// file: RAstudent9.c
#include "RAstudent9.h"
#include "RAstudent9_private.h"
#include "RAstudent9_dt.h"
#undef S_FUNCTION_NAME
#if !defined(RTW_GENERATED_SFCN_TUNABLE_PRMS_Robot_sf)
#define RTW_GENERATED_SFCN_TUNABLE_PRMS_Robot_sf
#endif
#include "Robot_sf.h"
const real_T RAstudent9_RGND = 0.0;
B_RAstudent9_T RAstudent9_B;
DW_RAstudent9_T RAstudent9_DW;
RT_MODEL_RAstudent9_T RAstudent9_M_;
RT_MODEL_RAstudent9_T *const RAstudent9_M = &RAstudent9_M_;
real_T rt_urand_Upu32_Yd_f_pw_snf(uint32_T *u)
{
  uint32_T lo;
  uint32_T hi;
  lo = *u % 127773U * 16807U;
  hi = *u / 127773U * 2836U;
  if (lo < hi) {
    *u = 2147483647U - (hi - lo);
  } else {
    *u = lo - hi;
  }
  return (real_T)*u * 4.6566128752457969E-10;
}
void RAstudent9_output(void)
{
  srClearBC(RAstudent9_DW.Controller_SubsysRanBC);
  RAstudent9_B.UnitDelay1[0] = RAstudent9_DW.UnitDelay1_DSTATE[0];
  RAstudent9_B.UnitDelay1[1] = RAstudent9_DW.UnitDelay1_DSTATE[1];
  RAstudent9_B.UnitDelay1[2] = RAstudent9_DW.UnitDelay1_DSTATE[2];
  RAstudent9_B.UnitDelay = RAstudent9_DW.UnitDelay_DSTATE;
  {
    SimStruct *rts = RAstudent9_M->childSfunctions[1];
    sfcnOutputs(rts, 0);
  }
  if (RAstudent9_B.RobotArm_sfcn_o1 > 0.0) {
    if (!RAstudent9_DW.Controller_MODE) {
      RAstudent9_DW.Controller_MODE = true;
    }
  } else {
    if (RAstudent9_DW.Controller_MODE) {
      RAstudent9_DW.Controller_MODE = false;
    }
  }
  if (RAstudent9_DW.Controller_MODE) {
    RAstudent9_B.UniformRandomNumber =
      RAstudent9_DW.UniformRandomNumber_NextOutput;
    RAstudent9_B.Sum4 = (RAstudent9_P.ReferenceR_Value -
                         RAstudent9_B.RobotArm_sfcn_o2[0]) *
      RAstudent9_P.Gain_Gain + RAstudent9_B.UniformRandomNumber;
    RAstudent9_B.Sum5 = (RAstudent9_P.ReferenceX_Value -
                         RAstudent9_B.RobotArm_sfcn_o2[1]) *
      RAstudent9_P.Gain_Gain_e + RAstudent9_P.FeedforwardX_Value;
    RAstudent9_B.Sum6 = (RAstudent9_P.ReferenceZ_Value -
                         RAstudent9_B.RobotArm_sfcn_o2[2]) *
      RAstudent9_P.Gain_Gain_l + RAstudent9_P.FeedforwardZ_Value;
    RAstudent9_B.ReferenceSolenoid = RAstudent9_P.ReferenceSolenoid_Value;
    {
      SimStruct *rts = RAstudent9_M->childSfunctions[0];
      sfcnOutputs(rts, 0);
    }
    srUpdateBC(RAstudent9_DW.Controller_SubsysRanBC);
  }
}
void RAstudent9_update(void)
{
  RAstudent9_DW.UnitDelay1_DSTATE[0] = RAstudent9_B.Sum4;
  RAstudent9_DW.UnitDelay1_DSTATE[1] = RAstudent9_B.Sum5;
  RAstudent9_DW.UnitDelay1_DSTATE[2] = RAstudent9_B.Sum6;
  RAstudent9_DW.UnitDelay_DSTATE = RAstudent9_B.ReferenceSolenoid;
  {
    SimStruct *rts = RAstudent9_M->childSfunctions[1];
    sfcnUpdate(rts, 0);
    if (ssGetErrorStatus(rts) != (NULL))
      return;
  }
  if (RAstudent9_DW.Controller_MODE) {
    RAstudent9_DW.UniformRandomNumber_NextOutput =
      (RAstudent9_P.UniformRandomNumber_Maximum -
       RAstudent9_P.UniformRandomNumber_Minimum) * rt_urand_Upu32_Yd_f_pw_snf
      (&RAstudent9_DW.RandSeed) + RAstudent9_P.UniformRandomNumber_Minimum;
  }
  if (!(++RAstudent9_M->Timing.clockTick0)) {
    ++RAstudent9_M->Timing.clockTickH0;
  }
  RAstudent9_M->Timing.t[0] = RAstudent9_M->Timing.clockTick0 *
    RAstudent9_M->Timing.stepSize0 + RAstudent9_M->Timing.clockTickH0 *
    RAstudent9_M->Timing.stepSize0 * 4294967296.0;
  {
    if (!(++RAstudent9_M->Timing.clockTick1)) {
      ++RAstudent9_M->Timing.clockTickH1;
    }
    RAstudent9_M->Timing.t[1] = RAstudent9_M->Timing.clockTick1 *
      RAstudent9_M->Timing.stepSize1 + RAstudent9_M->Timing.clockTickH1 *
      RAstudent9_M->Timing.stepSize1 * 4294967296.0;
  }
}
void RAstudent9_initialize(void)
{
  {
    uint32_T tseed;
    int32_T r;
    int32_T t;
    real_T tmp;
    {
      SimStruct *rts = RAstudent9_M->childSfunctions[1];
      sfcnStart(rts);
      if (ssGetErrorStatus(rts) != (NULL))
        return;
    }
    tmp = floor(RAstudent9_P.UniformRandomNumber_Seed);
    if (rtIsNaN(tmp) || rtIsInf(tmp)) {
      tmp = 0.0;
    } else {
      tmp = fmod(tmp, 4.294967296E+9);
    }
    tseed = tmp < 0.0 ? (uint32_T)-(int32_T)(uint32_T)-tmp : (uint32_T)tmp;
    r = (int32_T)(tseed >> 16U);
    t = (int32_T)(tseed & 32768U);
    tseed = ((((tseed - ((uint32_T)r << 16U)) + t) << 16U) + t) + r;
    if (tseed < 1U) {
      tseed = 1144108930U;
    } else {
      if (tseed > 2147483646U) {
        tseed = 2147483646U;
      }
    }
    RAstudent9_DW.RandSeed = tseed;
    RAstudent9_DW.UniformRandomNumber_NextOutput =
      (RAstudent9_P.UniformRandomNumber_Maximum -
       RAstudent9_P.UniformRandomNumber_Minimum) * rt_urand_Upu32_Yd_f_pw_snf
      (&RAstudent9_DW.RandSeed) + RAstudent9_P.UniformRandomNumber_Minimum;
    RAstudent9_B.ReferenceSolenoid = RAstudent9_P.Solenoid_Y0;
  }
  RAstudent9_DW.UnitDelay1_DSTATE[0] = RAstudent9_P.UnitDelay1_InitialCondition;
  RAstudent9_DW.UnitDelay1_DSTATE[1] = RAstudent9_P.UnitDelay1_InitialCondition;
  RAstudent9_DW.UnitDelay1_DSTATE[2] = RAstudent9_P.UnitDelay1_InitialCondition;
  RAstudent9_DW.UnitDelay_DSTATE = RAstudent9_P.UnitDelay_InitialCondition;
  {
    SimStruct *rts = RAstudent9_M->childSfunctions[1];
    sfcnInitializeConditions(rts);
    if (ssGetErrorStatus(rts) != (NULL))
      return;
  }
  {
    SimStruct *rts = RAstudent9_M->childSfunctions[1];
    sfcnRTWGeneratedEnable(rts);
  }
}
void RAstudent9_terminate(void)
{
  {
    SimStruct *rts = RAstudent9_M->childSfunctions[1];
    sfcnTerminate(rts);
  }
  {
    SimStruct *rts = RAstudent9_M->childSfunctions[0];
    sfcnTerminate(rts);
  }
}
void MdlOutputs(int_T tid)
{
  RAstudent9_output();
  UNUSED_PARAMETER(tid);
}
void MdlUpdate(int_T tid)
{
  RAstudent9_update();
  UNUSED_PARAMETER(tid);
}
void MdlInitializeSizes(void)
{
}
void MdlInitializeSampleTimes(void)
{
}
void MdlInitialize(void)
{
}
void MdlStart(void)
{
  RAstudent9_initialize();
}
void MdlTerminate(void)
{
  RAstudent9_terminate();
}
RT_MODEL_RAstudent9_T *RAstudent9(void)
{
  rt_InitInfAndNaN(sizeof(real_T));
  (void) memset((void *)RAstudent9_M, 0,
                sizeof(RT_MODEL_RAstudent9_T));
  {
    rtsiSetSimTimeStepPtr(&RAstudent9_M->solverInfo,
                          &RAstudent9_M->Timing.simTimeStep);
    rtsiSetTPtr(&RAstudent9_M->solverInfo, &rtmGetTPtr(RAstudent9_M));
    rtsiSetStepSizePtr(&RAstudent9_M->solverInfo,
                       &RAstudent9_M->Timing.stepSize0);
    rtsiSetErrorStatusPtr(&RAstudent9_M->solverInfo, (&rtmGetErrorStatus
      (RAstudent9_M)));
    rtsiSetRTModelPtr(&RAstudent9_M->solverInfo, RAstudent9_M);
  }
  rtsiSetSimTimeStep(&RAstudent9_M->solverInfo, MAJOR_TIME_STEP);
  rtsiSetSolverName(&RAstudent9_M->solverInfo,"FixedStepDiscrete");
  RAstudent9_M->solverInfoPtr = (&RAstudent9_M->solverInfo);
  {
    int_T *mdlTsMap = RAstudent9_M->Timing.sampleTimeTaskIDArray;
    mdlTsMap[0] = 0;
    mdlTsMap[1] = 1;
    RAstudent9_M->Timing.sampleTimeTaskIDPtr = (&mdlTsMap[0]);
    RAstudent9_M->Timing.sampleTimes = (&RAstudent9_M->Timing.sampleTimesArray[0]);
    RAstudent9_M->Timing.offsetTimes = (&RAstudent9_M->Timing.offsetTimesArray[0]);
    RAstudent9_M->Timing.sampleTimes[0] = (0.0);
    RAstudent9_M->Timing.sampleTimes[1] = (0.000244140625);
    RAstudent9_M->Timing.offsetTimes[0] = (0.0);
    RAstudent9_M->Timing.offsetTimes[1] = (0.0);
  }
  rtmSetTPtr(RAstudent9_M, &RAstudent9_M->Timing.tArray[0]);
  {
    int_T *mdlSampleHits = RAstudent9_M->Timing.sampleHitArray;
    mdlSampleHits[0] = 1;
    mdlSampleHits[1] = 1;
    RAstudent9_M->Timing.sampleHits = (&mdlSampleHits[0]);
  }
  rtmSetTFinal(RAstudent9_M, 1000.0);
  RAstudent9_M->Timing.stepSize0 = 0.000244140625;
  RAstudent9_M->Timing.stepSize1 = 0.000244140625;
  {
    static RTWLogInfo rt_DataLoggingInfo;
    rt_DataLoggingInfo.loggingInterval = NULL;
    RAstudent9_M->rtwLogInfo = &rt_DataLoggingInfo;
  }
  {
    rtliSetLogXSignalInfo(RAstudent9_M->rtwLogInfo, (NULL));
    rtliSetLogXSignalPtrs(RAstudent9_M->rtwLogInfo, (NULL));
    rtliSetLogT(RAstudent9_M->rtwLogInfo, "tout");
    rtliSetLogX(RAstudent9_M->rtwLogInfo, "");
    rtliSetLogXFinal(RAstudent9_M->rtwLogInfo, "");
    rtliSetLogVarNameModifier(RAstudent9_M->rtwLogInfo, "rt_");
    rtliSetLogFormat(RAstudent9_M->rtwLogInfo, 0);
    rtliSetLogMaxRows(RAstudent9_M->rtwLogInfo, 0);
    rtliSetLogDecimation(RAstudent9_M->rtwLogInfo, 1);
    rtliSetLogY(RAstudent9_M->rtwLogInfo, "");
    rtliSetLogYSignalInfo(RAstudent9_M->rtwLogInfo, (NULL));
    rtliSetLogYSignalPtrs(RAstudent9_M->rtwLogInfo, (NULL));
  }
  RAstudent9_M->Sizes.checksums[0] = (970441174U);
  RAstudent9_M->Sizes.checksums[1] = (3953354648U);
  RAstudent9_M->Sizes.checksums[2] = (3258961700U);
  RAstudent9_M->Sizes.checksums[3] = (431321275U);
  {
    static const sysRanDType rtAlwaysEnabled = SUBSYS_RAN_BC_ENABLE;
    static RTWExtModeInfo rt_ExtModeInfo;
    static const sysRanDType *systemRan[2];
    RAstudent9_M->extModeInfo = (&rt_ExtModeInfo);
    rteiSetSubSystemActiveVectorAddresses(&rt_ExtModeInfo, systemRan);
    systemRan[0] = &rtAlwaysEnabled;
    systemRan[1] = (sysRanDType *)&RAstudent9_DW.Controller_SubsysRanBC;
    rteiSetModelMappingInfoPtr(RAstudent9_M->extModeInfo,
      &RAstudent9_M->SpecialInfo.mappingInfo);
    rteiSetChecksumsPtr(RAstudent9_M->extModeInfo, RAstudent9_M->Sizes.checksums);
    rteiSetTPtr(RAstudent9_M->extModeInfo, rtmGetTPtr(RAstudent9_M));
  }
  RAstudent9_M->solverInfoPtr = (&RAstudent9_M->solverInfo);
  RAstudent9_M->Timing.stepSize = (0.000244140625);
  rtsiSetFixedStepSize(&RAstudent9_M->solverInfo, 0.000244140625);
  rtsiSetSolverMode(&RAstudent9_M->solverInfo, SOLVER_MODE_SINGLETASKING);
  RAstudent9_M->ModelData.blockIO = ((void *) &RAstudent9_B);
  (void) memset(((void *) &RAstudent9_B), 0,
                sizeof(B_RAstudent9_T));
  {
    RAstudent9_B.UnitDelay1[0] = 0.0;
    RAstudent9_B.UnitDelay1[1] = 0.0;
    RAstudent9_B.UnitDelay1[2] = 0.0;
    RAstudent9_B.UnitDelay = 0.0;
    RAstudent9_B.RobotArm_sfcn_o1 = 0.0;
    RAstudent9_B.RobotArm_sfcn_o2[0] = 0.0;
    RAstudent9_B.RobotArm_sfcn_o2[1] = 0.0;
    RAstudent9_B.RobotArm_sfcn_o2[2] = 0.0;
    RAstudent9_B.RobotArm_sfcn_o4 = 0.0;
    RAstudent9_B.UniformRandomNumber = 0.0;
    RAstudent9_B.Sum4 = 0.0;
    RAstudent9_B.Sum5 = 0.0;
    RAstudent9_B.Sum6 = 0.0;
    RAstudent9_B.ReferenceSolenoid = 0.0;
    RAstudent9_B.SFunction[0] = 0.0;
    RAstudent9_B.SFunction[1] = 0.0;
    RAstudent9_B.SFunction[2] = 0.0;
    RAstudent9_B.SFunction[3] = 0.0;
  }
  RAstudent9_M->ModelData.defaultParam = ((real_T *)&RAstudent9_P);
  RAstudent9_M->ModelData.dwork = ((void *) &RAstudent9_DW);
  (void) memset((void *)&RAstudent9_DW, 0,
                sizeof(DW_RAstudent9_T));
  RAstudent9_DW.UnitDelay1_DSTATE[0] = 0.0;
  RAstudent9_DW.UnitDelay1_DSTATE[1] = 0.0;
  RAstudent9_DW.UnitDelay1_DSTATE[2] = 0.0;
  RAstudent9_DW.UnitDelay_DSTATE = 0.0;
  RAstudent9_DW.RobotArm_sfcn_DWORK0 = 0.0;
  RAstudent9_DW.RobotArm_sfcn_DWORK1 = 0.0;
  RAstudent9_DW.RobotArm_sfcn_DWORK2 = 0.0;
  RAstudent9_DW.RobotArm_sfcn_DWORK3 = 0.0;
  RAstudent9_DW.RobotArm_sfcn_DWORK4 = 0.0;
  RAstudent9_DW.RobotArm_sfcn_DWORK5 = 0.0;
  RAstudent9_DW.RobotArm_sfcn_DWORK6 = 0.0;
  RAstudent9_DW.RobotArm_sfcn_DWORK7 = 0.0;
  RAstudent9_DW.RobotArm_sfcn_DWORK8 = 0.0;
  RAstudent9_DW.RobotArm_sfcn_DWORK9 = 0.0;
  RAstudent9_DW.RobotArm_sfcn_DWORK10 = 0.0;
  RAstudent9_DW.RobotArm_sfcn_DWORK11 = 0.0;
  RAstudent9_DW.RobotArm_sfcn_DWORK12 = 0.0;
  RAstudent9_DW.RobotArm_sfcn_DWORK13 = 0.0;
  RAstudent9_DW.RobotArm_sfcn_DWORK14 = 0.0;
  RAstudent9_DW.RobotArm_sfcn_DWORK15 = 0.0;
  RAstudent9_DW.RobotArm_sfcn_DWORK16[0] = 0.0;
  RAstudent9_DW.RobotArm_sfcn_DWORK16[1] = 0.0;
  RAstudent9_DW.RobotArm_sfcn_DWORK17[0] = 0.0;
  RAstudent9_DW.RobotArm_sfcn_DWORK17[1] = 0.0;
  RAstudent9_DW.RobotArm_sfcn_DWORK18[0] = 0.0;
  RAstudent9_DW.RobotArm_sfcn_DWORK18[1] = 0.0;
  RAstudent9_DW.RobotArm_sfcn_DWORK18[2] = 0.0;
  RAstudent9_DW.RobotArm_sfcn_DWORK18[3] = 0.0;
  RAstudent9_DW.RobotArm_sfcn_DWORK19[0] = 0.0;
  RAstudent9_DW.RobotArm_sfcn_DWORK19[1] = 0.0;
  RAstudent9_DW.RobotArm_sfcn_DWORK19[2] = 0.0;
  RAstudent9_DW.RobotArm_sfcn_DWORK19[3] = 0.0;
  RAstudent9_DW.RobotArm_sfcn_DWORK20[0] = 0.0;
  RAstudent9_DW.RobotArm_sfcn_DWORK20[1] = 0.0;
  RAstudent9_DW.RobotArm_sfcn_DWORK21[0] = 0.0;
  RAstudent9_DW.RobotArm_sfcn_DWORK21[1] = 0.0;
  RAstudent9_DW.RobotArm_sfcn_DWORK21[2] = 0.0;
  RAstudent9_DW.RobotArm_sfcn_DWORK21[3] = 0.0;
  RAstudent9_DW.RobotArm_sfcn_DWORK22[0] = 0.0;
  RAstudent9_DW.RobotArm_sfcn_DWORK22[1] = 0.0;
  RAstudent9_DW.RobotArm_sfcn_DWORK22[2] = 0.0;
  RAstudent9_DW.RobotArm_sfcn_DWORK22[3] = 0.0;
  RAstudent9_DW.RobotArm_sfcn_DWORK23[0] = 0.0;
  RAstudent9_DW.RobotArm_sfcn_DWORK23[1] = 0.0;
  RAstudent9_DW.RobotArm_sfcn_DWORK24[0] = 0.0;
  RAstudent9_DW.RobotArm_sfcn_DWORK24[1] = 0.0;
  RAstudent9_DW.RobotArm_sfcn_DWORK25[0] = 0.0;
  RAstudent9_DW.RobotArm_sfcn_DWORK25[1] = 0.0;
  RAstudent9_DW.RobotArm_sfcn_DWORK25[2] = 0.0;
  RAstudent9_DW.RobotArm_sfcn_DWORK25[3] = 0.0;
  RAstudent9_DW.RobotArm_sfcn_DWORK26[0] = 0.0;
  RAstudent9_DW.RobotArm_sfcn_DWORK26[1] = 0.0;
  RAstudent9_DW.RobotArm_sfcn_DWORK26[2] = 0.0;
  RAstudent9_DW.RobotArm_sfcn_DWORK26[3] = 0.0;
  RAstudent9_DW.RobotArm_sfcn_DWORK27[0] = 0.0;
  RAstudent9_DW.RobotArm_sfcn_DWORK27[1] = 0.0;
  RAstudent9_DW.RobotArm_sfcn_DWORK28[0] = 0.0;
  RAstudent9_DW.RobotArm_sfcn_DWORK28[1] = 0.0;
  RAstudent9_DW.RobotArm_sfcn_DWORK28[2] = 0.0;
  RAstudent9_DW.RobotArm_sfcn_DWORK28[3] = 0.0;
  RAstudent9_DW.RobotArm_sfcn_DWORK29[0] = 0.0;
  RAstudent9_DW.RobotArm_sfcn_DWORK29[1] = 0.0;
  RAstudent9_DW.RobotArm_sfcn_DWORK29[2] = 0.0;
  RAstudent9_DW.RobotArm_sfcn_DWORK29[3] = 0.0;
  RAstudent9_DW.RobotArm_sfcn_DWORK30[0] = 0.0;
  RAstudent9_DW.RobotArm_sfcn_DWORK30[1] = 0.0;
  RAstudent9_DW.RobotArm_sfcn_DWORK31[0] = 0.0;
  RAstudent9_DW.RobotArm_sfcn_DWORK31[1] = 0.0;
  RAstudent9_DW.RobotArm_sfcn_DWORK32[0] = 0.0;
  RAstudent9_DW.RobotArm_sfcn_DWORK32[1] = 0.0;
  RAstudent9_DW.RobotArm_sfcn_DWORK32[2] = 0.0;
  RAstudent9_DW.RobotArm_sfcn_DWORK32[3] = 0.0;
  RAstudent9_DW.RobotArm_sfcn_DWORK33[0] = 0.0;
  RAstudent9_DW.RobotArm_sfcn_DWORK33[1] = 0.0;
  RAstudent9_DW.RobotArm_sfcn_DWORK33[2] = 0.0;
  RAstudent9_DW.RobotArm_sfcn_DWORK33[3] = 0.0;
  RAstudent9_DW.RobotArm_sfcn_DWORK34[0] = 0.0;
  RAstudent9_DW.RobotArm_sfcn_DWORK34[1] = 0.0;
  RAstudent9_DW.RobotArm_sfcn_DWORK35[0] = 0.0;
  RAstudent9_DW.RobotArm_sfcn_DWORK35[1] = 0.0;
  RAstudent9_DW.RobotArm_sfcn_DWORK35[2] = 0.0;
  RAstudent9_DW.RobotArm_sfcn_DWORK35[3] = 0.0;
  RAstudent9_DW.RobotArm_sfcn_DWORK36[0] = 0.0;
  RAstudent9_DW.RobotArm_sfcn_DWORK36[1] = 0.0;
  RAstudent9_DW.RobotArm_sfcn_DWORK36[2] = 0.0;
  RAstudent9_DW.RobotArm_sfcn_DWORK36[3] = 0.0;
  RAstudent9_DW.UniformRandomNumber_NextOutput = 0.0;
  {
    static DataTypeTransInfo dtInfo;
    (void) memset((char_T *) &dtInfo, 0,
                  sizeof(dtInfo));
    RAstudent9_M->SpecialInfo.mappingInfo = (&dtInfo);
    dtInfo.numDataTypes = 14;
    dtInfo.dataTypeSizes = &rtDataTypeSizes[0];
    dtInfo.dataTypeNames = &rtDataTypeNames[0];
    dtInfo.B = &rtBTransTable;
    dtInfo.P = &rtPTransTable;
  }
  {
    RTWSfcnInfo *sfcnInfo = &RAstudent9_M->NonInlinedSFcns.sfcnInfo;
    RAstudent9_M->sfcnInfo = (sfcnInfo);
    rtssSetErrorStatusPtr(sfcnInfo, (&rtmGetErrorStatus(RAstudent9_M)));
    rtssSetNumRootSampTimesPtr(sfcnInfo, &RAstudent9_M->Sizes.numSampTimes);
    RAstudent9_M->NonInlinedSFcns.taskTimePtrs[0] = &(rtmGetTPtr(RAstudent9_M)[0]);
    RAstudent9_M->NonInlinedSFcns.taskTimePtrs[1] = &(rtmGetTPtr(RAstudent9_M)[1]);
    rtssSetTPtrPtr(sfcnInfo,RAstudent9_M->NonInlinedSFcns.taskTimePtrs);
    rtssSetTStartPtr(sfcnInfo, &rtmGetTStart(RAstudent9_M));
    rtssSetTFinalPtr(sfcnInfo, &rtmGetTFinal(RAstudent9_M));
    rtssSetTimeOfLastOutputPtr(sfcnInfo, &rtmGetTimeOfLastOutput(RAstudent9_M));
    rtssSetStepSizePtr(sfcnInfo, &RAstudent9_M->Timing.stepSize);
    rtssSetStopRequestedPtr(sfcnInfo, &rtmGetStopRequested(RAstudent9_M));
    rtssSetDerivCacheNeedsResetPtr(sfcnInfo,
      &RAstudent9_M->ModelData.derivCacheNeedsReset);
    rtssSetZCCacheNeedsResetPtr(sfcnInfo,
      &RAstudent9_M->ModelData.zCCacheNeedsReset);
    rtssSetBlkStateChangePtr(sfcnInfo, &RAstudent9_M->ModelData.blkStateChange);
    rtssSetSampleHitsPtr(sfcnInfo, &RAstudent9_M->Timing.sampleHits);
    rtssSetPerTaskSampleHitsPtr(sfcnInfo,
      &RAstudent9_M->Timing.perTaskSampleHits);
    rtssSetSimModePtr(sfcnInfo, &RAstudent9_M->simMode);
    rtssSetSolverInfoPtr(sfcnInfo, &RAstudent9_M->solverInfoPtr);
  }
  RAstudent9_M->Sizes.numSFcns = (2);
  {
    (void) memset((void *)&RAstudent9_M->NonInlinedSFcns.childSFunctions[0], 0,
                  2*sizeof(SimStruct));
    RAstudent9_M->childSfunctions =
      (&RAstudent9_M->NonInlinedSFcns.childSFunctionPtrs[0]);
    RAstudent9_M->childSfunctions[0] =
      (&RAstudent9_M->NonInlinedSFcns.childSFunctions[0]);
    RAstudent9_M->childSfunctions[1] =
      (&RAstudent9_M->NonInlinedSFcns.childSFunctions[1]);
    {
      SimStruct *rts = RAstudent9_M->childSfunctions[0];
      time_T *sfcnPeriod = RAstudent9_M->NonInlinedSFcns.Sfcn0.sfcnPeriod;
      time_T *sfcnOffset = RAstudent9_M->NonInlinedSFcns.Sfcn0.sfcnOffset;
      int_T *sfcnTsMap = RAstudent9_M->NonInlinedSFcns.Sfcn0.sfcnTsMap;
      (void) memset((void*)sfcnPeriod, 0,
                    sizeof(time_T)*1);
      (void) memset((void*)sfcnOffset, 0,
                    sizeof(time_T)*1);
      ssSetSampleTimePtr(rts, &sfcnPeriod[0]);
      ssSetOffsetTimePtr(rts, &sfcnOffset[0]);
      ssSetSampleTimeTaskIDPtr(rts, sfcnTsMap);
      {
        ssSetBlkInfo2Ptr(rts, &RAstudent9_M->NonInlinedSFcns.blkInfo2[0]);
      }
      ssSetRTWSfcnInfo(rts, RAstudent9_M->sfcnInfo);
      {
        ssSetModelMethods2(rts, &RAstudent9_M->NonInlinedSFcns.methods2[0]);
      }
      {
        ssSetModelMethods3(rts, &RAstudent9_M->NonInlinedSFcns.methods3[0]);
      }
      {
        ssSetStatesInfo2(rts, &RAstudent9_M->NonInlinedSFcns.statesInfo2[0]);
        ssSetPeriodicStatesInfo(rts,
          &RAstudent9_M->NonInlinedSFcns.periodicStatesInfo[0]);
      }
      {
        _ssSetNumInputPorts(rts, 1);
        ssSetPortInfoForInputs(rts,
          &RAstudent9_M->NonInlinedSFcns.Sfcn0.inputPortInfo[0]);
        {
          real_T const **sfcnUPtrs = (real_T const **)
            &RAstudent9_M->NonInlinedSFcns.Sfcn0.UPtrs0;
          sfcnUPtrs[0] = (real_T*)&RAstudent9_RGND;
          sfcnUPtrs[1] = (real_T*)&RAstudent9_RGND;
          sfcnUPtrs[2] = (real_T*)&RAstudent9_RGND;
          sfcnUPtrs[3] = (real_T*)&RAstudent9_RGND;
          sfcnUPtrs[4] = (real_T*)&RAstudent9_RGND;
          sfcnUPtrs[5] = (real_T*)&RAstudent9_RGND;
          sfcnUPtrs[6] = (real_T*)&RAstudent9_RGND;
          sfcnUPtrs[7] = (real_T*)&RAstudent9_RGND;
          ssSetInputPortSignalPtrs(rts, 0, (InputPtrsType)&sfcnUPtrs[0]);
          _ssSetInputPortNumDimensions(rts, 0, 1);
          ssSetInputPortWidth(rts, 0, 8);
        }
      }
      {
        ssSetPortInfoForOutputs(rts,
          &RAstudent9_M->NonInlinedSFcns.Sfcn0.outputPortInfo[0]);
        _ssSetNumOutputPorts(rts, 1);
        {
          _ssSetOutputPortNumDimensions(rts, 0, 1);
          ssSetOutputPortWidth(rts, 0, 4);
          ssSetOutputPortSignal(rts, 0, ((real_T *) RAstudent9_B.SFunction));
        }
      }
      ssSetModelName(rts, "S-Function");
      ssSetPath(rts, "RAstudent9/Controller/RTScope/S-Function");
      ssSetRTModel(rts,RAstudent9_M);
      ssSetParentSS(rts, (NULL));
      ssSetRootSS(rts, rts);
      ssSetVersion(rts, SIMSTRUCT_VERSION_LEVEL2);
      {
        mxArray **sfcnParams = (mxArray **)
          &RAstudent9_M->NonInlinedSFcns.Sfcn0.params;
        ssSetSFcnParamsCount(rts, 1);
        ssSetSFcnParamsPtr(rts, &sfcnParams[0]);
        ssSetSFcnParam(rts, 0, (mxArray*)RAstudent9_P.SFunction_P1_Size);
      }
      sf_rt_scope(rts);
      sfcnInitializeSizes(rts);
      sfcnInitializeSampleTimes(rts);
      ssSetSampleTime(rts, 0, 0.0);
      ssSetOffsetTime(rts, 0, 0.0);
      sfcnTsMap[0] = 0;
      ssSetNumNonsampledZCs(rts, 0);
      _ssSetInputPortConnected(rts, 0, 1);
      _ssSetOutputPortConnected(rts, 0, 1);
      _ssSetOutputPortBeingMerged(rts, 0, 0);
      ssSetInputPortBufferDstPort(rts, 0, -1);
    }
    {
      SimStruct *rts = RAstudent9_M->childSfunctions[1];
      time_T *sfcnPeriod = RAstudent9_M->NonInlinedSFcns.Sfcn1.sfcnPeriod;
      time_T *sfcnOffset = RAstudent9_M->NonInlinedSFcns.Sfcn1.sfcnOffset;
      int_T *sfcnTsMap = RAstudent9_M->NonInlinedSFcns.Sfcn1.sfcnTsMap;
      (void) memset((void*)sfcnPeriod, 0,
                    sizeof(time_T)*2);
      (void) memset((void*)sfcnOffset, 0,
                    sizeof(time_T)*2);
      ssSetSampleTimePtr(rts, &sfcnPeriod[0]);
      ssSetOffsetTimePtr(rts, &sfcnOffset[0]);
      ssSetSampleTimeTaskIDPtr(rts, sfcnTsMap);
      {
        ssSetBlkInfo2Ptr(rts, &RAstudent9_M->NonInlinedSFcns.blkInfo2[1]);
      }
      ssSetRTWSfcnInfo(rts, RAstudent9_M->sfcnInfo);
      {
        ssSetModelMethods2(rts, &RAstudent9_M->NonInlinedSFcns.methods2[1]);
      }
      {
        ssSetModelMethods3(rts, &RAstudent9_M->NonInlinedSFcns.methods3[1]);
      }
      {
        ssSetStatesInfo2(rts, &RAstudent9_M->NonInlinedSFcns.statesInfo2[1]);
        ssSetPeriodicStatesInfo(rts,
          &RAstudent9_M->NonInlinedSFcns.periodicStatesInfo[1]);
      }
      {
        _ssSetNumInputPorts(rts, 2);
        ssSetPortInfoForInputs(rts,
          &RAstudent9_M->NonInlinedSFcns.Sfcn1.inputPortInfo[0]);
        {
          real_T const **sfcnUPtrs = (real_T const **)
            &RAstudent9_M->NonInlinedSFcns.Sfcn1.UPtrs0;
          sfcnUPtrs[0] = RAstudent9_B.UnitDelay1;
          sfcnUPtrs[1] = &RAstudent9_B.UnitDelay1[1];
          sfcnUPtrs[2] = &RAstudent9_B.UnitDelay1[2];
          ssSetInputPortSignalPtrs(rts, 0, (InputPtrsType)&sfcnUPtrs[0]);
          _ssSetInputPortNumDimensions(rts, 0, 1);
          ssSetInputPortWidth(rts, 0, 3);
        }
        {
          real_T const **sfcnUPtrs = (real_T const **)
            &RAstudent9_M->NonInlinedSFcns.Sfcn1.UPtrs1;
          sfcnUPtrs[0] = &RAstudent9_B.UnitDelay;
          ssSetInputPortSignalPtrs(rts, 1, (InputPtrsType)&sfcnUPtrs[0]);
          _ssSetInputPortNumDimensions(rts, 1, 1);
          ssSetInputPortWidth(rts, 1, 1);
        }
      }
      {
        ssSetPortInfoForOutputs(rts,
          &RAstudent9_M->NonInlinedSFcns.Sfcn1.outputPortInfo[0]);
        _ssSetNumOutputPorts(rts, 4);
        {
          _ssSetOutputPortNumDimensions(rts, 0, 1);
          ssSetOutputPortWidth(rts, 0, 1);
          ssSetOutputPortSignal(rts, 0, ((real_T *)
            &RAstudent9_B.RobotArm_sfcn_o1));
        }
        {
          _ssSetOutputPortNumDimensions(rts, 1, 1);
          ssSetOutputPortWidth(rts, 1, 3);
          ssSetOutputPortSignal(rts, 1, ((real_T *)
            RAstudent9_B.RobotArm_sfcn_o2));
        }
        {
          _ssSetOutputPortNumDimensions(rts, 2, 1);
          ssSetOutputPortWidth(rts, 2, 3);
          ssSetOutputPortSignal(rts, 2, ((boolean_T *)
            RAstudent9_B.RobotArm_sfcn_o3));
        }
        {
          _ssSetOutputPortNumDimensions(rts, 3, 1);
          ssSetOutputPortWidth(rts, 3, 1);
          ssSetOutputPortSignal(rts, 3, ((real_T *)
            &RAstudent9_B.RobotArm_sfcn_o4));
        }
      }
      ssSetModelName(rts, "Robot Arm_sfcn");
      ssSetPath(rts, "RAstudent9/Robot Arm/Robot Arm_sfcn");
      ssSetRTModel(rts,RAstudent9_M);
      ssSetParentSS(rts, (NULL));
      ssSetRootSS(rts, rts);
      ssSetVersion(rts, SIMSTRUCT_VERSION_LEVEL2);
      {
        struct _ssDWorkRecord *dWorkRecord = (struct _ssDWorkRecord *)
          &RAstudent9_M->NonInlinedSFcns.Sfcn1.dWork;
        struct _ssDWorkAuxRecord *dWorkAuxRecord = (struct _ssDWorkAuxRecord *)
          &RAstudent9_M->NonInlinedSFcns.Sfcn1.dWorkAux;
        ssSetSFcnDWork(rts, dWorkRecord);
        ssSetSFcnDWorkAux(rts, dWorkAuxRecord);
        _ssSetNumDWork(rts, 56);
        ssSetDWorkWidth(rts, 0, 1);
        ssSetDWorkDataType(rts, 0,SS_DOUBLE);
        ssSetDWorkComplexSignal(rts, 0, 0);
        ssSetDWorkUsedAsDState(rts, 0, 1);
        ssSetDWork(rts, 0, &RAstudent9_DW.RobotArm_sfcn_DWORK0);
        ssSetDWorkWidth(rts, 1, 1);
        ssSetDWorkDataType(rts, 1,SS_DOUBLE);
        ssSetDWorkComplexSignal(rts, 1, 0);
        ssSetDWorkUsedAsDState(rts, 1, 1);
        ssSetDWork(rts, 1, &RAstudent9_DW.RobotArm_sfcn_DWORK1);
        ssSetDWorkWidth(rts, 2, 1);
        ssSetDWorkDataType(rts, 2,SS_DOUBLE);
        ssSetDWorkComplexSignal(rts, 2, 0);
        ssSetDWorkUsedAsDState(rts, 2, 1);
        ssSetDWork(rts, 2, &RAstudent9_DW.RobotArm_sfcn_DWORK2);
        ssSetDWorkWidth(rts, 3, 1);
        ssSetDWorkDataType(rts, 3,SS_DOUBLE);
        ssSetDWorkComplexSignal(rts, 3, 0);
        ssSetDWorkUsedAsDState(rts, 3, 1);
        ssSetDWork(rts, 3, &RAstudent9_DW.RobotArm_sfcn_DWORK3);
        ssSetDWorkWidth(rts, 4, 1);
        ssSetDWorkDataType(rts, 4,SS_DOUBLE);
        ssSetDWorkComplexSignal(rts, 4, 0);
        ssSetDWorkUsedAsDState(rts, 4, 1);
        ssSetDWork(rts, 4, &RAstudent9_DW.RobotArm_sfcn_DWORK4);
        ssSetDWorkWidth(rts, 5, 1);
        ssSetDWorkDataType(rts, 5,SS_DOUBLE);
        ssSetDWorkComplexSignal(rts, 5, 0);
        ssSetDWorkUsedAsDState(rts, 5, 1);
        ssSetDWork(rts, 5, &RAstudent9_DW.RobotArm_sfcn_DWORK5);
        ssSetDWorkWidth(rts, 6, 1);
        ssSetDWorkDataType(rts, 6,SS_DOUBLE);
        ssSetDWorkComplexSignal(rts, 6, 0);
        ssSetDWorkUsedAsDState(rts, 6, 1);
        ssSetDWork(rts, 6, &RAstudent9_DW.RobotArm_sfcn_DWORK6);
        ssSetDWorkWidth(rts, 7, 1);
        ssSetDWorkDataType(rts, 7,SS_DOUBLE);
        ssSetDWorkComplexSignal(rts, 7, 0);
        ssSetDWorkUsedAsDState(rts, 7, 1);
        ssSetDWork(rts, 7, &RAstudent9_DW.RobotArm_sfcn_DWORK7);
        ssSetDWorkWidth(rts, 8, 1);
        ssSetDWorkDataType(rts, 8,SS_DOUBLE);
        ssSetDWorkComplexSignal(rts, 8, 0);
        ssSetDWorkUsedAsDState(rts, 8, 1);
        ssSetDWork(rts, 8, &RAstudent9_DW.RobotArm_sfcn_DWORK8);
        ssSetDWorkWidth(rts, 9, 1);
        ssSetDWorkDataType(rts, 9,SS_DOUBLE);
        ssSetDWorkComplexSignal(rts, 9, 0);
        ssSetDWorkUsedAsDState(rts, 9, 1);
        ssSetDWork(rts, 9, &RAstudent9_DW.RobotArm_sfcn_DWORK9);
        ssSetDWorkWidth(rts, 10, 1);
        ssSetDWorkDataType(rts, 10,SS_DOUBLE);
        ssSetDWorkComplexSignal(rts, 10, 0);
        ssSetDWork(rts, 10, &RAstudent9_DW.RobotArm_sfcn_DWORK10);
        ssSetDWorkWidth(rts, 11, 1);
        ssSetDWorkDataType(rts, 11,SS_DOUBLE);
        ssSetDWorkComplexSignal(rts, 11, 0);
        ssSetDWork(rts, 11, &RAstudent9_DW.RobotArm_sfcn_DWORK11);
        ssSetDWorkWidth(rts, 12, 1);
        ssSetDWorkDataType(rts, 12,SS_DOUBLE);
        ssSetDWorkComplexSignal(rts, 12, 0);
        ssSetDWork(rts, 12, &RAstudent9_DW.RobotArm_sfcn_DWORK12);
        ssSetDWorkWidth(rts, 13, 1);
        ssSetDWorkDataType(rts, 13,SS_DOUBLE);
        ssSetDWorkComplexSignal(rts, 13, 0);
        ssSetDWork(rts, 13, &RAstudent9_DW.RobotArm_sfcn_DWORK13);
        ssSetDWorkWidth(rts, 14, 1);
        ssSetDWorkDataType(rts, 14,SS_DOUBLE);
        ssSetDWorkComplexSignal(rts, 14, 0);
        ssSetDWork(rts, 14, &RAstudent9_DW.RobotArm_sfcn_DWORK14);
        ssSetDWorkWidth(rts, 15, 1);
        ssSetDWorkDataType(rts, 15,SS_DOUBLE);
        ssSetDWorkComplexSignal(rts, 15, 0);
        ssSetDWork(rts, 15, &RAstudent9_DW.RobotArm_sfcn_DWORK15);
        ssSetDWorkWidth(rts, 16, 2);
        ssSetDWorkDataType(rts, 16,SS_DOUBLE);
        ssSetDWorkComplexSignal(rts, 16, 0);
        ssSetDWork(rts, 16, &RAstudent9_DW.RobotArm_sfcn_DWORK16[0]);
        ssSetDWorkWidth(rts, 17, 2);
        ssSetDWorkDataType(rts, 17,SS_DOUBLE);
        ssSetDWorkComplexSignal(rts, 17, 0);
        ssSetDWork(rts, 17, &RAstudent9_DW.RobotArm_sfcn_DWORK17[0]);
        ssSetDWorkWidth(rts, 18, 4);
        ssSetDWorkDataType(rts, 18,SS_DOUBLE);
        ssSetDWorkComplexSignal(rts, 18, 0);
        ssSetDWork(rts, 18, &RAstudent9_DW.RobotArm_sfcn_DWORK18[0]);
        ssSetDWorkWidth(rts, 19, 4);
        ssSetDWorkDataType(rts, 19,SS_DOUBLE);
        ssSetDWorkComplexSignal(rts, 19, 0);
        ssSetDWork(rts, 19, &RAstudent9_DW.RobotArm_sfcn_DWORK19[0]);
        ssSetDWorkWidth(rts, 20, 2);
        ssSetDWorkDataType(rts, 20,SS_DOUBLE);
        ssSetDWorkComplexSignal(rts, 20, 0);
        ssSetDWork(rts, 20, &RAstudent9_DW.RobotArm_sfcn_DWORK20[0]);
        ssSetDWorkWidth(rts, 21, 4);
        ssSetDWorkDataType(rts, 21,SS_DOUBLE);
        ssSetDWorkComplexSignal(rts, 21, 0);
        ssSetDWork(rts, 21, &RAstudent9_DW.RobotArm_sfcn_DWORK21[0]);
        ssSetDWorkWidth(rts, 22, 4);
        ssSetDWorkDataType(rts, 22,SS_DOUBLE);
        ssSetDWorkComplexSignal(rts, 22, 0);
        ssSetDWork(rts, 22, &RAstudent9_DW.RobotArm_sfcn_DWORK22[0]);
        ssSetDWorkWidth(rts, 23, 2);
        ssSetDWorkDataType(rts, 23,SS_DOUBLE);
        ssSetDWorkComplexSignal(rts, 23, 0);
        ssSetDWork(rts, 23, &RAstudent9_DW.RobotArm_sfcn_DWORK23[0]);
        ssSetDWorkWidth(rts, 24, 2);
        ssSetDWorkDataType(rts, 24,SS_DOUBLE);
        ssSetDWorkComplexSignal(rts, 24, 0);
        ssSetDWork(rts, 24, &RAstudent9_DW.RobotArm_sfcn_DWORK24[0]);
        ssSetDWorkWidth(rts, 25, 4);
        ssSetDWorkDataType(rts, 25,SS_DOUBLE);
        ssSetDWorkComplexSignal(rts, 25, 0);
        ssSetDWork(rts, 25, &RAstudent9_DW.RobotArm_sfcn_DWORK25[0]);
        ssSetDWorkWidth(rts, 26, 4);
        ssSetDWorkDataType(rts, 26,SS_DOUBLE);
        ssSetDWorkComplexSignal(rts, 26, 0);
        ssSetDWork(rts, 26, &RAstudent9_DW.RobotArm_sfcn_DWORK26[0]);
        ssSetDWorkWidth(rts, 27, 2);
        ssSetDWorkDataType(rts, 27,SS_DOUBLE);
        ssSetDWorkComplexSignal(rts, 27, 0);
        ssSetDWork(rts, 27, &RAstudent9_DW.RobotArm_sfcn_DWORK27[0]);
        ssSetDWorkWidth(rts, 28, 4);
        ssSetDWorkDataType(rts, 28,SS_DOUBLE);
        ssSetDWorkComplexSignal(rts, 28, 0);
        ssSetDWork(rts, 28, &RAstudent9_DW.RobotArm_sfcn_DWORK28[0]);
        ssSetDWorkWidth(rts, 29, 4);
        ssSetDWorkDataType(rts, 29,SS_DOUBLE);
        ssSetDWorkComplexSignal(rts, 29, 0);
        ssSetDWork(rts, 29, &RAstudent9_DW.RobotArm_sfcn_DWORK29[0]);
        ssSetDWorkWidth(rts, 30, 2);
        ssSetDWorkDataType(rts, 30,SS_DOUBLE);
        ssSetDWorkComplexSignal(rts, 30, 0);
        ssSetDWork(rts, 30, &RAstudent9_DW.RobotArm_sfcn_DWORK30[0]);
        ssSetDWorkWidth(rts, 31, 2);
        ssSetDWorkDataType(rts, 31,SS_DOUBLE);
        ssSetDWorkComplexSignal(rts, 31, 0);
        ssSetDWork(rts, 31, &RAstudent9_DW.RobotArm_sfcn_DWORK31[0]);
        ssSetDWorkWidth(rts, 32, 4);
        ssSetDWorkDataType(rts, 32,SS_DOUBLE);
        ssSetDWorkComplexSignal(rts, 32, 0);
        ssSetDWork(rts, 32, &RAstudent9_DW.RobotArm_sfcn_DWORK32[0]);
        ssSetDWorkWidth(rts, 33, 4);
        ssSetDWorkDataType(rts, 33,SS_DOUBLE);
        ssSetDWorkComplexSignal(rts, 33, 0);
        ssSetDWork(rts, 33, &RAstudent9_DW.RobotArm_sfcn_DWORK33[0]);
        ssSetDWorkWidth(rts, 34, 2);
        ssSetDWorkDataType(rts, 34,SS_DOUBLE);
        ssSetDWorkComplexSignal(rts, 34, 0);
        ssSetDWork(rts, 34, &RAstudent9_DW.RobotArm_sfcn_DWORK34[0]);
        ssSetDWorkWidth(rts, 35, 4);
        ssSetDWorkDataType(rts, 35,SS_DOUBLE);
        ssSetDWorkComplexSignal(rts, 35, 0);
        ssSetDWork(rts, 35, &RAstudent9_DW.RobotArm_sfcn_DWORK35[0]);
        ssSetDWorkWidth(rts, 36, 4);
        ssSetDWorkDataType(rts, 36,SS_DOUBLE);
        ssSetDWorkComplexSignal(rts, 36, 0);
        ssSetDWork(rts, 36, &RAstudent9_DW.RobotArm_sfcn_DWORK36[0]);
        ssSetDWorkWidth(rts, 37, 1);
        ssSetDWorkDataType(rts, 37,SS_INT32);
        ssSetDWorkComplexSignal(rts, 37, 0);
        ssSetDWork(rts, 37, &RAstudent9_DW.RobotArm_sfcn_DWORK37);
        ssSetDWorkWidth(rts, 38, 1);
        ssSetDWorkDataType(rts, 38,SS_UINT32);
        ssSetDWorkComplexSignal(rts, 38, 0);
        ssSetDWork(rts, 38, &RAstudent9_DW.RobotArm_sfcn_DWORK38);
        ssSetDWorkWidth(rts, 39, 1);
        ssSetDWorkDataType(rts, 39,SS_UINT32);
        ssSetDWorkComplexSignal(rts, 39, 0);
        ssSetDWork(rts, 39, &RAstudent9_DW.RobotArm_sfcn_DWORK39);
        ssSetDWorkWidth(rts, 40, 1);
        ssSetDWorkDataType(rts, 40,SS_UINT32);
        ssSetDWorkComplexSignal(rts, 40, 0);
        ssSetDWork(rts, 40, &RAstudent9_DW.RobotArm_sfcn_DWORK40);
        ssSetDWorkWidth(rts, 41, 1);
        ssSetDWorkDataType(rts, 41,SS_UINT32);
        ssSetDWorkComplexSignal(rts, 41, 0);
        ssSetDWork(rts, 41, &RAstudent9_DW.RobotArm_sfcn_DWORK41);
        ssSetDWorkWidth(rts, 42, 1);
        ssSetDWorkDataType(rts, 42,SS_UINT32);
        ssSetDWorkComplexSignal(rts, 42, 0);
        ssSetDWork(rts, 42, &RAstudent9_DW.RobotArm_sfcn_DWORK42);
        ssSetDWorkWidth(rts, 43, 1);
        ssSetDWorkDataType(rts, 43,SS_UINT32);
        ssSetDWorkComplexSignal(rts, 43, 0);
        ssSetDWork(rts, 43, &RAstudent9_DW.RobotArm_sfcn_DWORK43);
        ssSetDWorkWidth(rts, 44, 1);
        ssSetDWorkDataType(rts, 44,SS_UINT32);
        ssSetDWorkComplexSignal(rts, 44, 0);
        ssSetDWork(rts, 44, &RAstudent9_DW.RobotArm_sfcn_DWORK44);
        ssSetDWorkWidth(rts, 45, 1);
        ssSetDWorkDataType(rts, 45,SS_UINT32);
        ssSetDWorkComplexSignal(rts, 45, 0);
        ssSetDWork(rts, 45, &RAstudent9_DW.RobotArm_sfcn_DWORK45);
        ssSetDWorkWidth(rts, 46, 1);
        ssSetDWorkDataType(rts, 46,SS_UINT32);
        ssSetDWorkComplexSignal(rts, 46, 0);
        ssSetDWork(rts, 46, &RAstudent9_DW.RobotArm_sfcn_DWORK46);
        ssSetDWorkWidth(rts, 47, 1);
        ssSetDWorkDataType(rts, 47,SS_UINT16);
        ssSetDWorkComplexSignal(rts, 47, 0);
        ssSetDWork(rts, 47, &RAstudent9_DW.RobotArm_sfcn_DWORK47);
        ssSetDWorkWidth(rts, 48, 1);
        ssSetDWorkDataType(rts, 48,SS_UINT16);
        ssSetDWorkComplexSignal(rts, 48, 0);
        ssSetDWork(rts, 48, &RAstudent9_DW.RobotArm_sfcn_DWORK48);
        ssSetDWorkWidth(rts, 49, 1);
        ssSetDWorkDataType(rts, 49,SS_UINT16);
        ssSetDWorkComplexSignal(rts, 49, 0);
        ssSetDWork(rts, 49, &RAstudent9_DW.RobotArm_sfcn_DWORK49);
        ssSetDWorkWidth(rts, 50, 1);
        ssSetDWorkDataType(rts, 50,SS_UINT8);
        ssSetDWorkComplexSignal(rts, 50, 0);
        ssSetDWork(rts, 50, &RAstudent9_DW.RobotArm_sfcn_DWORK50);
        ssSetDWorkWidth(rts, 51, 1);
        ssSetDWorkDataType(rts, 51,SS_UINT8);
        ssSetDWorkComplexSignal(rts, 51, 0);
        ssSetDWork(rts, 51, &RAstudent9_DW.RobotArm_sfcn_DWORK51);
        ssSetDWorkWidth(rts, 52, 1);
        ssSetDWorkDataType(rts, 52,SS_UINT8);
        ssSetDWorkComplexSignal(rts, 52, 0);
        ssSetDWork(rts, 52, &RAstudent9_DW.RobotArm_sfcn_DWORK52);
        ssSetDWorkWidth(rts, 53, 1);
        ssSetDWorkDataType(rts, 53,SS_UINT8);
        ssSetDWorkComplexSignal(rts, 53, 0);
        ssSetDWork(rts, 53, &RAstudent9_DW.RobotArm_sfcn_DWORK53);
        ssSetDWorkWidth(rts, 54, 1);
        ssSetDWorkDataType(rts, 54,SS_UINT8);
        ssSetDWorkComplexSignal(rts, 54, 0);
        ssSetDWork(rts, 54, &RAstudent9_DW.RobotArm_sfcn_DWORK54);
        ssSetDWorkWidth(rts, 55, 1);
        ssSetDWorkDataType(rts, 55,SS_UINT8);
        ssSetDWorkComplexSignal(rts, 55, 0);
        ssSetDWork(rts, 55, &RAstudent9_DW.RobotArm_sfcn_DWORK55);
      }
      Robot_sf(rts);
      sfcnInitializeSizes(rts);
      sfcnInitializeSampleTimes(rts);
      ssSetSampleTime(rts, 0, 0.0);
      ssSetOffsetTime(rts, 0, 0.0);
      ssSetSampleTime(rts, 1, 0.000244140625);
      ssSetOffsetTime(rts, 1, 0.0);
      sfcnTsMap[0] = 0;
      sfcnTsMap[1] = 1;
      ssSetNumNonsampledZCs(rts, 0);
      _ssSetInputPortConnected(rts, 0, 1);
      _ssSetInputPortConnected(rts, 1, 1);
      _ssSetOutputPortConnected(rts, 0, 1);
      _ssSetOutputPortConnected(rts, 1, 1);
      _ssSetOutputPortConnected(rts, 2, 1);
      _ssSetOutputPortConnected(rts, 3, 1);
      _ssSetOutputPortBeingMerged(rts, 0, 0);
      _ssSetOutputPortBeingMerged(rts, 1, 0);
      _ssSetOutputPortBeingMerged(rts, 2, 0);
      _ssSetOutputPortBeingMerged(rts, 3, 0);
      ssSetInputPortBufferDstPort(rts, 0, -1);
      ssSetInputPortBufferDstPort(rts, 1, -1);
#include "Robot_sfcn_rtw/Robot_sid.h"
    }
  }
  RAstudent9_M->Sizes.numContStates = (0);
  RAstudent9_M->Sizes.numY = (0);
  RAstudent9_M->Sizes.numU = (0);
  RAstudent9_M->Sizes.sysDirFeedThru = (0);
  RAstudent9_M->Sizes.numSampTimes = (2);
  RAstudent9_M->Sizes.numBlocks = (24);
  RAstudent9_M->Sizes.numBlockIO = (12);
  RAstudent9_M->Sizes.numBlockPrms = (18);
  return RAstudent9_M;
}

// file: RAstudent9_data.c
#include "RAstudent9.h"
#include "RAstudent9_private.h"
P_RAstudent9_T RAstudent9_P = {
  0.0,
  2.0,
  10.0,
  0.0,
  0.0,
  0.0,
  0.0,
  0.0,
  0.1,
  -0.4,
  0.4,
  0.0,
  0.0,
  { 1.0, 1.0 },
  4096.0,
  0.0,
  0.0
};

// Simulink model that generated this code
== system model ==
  UnitDelay1 : UnitDelay  <- 1: Controller
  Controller : Subsystem  <- 1: RobotArm_sfcn/2, Enable: RobotArm_sfcn
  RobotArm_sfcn : S-Function  FunctionName=Robot_sf  <- 1: UnitDelay1, 2: UnitDelay
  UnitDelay : UnitDelay  <- 1: Controller/2
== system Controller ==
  Inport#1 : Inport
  EnablePort#1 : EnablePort
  Outport#1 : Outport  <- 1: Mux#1
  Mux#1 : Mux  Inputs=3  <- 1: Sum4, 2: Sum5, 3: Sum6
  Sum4 : Sum  Inputs=++  <- 1: UniformRandomNumber, 2: Gain
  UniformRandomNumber : UniformRandomNumber
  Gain : Gain  Gain=10  <- 1: Sum#1
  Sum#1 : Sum  Inputs=+-  <- 1: ReferenceR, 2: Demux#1
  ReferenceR : Constant  Value=2
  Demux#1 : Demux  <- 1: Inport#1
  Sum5 : Sum  Inputs=++  <- 1: FeedforwardX, 2: Gain#1
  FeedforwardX : Constant  Value=0
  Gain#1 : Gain  Gain=0  <- 1: Sum#2
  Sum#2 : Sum  Inputs=+-  <- 1: ReferenceX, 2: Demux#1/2
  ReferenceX : Constant  Value=0
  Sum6 : Sum  Inputs=++  <- 1: FeedforwardZ, 2: Gain#2
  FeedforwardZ : Constant  Value=0.1
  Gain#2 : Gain  Gain=0  <- 1: Sum#3
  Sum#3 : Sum  Inputs=+-  <- 1: ReferenceZ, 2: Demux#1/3
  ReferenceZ : Constant  Value=0
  Solenoid : Outport  InitialOutput=0  <- 1: ReferenceSolenoid
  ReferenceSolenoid : Constant  Value=0
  SFunction : S-Function  FunctionName=sf_rt_scope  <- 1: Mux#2
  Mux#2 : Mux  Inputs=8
